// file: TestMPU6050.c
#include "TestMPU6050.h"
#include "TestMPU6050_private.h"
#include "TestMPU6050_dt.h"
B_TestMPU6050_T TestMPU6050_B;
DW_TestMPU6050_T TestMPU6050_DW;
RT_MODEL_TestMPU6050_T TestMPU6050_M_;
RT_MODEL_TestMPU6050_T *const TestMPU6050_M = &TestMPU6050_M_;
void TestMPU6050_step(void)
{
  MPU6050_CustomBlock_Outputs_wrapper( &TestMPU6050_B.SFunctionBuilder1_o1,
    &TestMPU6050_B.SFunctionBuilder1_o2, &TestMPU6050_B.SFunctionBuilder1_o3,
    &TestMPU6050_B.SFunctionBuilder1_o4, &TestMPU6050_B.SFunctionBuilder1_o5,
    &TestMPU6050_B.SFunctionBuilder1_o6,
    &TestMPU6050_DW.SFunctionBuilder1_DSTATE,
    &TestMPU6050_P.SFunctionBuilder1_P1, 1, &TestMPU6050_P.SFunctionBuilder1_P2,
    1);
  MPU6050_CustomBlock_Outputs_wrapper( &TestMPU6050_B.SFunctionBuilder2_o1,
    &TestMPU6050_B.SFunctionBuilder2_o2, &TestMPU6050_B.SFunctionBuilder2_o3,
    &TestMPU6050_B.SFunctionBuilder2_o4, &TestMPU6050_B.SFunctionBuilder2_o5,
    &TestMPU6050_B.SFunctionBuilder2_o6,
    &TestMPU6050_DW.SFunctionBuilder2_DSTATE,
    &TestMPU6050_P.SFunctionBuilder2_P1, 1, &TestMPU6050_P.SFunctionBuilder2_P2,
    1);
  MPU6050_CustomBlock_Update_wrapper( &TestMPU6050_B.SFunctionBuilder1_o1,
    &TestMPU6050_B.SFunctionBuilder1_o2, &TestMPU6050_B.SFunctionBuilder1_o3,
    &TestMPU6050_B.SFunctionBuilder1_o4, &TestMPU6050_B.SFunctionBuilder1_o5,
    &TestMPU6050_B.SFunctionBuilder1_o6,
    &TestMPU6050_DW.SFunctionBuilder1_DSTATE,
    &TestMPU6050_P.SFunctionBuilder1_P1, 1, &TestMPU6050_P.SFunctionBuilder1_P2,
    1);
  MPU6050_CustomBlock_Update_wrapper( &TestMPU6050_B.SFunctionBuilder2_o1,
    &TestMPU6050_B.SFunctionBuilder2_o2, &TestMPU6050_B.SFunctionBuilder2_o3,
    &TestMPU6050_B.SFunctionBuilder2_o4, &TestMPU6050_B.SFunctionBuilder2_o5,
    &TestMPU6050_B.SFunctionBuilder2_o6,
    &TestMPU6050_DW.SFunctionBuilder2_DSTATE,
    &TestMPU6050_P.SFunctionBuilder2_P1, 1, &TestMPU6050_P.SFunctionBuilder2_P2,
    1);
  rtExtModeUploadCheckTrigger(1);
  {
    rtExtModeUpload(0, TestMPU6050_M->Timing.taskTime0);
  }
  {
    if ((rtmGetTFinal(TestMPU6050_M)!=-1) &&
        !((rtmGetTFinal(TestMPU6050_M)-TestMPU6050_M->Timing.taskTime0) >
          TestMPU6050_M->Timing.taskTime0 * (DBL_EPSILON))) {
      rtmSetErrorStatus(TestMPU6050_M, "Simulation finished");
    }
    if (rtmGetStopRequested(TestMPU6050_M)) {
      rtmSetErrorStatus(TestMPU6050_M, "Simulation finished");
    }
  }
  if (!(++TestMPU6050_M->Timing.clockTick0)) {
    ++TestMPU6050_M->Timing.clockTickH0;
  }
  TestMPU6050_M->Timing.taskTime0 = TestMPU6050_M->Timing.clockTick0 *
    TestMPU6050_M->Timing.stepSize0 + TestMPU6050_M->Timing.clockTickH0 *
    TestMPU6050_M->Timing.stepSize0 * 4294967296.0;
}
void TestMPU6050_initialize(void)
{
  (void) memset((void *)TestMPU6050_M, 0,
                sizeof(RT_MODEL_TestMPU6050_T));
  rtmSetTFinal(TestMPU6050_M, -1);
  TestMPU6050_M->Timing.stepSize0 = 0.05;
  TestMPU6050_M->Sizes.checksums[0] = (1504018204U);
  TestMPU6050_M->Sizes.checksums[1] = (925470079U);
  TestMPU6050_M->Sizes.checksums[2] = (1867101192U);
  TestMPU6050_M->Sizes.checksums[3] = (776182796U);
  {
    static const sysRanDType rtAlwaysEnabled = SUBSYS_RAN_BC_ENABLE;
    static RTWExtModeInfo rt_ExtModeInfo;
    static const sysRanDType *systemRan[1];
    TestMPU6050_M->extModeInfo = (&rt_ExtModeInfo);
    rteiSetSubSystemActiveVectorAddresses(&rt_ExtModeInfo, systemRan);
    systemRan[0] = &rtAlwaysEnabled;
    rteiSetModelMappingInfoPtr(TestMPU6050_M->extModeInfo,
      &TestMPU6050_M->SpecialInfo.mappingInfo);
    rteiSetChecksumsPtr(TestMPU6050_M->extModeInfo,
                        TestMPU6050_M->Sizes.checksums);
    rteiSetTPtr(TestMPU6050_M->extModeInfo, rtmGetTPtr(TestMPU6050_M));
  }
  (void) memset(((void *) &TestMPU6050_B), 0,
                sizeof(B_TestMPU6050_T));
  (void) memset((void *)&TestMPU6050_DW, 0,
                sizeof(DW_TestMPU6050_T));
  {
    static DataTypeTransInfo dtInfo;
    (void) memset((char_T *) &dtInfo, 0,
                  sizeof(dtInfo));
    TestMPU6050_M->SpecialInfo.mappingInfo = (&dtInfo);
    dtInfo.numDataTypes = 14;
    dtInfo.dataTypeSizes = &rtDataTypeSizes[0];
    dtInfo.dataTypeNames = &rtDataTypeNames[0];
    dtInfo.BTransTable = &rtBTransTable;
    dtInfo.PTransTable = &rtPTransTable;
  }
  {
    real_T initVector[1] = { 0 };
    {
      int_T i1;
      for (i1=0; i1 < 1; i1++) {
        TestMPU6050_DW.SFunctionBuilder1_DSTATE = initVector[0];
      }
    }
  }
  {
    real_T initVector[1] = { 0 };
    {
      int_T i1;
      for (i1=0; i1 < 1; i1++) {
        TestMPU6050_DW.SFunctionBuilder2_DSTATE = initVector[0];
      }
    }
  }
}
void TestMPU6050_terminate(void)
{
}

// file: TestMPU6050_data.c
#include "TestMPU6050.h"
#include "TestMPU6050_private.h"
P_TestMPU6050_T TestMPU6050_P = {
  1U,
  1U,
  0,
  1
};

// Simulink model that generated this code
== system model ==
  SFunctionBuilder1 : S-Function  FunctionName=MPU6050_CustomBlock
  SFunctionBuilder2 : S-Function  FunctionName=MPU6050_CustomBlock
